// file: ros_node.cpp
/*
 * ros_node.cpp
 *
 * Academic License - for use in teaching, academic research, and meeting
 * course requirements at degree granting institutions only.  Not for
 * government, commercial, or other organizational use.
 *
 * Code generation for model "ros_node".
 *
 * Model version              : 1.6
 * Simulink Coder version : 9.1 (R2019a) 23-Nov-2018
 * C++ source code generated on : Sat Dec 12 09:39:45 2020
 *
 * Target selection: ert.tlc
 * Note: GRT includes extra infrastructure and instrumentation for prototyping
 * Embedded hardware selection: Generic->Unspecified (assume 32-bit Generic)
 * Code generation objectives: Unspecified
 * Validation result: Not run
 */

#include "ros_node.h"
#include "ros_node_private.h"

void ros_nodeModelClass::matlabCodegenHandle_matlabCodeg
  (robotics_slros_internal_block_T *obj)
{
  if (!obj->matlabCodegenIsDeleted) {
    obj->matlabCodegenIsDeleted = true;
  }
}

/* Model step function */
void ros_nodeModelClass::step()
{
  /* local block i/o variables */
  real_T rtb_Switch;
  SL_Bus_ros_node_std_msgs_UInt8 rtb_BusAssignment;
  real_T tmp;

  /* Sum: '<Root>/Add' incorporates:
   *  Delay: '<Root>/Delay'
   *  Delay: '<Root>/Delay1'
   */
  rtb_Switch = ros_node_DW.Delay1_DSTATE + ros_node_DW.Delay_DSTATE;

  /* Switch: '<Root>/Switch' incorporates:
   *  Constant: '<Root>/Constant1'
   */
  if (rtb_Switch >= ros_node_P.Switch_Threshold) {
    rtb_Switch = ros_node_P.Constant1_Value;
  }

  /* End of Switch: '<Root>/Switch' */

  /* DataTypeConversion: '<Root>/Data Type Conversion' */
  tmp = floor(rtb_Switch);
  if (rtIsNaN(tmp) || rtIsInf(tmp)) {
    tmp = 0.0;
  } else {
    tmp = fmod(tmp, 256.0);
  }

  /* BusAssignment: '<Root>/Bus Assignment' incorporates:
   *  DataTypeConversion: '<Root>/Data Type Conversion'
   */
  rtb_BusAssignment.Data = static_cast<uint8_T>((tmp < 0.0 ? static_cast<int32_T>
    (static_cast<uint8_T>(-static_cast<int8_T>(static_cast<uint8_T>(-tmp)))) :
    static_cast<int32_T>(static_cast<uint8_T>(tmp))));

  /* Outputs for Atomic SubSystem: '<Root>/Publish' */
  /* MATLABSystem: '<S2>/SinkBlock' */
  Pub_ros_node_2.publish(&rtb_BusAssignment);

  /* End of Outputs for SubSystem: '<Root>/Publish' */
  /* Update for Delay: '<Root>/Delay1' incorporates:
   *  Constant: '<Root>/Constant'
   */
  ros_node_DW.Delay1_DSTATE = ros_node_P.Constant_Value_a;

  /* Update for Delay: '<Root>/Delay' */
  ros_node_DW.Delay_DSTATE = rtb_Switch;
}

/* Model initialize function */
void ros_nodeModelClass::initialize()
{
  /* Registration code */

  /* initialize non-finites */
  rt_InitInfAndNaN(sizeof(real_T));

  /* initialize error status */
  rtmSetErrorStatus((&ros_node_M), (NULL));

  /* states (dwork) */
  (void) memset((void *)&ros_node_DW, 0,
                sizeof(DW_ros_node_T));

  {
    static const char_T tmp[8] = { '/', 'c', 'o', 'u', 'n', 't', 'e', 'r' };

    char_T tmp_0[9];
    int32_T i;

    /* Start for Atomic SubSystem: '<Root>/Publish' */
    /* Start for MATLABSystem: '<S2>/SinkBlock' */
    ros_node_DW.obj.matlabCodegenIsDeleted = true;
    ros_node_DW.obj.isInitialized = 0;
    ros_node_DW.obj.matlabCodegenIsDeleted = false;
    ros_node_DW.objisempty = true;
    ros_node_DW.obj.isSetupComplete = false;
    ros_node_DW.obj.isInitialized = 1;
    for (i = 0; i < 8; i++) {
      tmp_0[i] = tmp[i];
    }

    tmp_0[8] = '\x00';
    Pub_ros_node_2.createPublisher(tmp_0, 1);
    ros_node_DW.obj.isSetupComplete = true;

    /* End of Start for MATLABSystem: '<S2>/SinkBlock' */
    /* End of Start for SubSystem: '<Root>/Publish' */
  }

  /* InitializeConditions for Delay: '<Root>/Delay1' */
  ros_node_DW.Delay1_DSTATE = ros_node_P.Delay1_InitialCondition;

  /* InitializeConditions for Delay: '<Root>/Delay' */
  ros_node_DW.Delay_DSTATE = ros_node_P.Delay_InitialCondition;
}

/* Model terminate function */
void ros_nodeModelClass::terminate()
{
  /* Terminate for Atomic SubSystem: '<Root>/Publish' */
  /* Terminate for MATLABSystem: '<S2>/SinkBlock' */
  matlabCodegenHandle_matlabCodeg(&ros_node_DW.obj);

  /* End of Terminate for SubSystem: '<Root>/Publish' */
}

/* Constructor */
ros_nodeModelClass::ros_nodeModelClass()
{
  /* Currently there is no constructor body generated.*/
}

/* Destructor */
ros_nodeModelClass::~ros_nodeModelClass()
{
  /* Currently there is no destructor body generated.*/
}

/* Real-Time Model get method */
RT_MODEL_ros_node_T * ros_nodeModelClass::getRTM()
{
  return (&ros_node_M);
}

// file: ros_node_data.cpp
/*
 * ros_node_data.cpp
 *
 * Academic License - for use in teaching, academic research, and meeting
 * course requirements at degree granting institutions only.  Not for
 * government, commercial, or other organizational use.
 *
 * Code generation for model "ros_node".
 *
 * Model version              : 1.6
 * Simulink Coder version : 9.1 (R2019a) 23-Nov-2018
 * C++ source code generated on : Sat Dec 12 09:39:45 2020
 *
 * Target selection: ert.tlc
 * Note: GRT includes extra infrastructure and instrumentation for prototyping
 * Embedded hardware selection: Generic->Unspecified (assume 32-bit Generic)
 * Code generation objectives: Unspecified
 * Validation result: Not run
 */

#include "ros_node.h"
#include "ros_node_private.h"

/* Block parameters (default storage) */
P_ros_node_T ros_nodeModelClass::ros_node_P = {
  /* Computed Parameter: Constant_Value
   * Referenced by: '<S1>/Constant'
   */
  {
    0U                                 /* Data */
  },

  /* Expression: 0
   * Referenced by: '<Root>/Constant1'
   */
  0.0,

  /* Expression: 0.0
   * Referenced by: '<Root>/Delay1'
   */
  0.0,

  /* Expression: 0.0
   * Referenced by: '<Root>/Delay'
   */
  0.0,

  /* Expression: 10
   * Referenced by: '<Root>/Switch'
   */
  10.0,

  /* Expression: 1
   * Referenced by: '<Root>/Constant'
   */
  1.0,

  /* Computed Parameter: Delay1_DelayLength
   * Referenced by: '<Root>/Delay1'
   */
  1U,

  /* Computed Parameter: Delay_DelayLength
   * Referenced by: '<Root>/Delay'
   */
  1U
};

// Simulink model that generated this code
simulink model "ros_node"  (R2019a)
settings: Solver=FixedStepAuto  StartTime=0.0  StopTime=10.0  RelTol=1e-3
libraries: robotlib x2

== system ros_node ==
  Add : Sum
  Blank Message : robotlib/Blank Message  messageClass=Message  entityType=std_msgs/UInt8  messageType=std_msgs/UInt8  SampleTime=inf
  Bus Assignment : BusAssignment  AssignedSignals=Data
  Constant : Constant
  Constant1 : Constant  Value=0
  Data Type Conversion : DataTypeConversion
  Delay : Delay  DelayLength=1
  Delay1 : Delay  DelayLength=1
  Publish : robotlib/Publish  topicSource=Specify your own  topic=/counter  messageType=std_msgs/UInt8  messageQueueLength=1
  Scope : Scope
  Switch : Switch  Threshold=10
  wires:
  Bus Assignment/1 -> Publish/1
  Blank Message/1 -> Bus Assignment/1
  Data Type Conversion/1 -> Bus Assignment/2
  Constant/1 -> Delay1/1
  Constant1/1 -> Switch/1
  Add/1 -> Switch/3, Switch/2
  Switch/1 -> Delay/1, Data Type Conversion/1, Scope/1
  Delay/1 -> Add/2
  Delay1/1 -> Add/1
